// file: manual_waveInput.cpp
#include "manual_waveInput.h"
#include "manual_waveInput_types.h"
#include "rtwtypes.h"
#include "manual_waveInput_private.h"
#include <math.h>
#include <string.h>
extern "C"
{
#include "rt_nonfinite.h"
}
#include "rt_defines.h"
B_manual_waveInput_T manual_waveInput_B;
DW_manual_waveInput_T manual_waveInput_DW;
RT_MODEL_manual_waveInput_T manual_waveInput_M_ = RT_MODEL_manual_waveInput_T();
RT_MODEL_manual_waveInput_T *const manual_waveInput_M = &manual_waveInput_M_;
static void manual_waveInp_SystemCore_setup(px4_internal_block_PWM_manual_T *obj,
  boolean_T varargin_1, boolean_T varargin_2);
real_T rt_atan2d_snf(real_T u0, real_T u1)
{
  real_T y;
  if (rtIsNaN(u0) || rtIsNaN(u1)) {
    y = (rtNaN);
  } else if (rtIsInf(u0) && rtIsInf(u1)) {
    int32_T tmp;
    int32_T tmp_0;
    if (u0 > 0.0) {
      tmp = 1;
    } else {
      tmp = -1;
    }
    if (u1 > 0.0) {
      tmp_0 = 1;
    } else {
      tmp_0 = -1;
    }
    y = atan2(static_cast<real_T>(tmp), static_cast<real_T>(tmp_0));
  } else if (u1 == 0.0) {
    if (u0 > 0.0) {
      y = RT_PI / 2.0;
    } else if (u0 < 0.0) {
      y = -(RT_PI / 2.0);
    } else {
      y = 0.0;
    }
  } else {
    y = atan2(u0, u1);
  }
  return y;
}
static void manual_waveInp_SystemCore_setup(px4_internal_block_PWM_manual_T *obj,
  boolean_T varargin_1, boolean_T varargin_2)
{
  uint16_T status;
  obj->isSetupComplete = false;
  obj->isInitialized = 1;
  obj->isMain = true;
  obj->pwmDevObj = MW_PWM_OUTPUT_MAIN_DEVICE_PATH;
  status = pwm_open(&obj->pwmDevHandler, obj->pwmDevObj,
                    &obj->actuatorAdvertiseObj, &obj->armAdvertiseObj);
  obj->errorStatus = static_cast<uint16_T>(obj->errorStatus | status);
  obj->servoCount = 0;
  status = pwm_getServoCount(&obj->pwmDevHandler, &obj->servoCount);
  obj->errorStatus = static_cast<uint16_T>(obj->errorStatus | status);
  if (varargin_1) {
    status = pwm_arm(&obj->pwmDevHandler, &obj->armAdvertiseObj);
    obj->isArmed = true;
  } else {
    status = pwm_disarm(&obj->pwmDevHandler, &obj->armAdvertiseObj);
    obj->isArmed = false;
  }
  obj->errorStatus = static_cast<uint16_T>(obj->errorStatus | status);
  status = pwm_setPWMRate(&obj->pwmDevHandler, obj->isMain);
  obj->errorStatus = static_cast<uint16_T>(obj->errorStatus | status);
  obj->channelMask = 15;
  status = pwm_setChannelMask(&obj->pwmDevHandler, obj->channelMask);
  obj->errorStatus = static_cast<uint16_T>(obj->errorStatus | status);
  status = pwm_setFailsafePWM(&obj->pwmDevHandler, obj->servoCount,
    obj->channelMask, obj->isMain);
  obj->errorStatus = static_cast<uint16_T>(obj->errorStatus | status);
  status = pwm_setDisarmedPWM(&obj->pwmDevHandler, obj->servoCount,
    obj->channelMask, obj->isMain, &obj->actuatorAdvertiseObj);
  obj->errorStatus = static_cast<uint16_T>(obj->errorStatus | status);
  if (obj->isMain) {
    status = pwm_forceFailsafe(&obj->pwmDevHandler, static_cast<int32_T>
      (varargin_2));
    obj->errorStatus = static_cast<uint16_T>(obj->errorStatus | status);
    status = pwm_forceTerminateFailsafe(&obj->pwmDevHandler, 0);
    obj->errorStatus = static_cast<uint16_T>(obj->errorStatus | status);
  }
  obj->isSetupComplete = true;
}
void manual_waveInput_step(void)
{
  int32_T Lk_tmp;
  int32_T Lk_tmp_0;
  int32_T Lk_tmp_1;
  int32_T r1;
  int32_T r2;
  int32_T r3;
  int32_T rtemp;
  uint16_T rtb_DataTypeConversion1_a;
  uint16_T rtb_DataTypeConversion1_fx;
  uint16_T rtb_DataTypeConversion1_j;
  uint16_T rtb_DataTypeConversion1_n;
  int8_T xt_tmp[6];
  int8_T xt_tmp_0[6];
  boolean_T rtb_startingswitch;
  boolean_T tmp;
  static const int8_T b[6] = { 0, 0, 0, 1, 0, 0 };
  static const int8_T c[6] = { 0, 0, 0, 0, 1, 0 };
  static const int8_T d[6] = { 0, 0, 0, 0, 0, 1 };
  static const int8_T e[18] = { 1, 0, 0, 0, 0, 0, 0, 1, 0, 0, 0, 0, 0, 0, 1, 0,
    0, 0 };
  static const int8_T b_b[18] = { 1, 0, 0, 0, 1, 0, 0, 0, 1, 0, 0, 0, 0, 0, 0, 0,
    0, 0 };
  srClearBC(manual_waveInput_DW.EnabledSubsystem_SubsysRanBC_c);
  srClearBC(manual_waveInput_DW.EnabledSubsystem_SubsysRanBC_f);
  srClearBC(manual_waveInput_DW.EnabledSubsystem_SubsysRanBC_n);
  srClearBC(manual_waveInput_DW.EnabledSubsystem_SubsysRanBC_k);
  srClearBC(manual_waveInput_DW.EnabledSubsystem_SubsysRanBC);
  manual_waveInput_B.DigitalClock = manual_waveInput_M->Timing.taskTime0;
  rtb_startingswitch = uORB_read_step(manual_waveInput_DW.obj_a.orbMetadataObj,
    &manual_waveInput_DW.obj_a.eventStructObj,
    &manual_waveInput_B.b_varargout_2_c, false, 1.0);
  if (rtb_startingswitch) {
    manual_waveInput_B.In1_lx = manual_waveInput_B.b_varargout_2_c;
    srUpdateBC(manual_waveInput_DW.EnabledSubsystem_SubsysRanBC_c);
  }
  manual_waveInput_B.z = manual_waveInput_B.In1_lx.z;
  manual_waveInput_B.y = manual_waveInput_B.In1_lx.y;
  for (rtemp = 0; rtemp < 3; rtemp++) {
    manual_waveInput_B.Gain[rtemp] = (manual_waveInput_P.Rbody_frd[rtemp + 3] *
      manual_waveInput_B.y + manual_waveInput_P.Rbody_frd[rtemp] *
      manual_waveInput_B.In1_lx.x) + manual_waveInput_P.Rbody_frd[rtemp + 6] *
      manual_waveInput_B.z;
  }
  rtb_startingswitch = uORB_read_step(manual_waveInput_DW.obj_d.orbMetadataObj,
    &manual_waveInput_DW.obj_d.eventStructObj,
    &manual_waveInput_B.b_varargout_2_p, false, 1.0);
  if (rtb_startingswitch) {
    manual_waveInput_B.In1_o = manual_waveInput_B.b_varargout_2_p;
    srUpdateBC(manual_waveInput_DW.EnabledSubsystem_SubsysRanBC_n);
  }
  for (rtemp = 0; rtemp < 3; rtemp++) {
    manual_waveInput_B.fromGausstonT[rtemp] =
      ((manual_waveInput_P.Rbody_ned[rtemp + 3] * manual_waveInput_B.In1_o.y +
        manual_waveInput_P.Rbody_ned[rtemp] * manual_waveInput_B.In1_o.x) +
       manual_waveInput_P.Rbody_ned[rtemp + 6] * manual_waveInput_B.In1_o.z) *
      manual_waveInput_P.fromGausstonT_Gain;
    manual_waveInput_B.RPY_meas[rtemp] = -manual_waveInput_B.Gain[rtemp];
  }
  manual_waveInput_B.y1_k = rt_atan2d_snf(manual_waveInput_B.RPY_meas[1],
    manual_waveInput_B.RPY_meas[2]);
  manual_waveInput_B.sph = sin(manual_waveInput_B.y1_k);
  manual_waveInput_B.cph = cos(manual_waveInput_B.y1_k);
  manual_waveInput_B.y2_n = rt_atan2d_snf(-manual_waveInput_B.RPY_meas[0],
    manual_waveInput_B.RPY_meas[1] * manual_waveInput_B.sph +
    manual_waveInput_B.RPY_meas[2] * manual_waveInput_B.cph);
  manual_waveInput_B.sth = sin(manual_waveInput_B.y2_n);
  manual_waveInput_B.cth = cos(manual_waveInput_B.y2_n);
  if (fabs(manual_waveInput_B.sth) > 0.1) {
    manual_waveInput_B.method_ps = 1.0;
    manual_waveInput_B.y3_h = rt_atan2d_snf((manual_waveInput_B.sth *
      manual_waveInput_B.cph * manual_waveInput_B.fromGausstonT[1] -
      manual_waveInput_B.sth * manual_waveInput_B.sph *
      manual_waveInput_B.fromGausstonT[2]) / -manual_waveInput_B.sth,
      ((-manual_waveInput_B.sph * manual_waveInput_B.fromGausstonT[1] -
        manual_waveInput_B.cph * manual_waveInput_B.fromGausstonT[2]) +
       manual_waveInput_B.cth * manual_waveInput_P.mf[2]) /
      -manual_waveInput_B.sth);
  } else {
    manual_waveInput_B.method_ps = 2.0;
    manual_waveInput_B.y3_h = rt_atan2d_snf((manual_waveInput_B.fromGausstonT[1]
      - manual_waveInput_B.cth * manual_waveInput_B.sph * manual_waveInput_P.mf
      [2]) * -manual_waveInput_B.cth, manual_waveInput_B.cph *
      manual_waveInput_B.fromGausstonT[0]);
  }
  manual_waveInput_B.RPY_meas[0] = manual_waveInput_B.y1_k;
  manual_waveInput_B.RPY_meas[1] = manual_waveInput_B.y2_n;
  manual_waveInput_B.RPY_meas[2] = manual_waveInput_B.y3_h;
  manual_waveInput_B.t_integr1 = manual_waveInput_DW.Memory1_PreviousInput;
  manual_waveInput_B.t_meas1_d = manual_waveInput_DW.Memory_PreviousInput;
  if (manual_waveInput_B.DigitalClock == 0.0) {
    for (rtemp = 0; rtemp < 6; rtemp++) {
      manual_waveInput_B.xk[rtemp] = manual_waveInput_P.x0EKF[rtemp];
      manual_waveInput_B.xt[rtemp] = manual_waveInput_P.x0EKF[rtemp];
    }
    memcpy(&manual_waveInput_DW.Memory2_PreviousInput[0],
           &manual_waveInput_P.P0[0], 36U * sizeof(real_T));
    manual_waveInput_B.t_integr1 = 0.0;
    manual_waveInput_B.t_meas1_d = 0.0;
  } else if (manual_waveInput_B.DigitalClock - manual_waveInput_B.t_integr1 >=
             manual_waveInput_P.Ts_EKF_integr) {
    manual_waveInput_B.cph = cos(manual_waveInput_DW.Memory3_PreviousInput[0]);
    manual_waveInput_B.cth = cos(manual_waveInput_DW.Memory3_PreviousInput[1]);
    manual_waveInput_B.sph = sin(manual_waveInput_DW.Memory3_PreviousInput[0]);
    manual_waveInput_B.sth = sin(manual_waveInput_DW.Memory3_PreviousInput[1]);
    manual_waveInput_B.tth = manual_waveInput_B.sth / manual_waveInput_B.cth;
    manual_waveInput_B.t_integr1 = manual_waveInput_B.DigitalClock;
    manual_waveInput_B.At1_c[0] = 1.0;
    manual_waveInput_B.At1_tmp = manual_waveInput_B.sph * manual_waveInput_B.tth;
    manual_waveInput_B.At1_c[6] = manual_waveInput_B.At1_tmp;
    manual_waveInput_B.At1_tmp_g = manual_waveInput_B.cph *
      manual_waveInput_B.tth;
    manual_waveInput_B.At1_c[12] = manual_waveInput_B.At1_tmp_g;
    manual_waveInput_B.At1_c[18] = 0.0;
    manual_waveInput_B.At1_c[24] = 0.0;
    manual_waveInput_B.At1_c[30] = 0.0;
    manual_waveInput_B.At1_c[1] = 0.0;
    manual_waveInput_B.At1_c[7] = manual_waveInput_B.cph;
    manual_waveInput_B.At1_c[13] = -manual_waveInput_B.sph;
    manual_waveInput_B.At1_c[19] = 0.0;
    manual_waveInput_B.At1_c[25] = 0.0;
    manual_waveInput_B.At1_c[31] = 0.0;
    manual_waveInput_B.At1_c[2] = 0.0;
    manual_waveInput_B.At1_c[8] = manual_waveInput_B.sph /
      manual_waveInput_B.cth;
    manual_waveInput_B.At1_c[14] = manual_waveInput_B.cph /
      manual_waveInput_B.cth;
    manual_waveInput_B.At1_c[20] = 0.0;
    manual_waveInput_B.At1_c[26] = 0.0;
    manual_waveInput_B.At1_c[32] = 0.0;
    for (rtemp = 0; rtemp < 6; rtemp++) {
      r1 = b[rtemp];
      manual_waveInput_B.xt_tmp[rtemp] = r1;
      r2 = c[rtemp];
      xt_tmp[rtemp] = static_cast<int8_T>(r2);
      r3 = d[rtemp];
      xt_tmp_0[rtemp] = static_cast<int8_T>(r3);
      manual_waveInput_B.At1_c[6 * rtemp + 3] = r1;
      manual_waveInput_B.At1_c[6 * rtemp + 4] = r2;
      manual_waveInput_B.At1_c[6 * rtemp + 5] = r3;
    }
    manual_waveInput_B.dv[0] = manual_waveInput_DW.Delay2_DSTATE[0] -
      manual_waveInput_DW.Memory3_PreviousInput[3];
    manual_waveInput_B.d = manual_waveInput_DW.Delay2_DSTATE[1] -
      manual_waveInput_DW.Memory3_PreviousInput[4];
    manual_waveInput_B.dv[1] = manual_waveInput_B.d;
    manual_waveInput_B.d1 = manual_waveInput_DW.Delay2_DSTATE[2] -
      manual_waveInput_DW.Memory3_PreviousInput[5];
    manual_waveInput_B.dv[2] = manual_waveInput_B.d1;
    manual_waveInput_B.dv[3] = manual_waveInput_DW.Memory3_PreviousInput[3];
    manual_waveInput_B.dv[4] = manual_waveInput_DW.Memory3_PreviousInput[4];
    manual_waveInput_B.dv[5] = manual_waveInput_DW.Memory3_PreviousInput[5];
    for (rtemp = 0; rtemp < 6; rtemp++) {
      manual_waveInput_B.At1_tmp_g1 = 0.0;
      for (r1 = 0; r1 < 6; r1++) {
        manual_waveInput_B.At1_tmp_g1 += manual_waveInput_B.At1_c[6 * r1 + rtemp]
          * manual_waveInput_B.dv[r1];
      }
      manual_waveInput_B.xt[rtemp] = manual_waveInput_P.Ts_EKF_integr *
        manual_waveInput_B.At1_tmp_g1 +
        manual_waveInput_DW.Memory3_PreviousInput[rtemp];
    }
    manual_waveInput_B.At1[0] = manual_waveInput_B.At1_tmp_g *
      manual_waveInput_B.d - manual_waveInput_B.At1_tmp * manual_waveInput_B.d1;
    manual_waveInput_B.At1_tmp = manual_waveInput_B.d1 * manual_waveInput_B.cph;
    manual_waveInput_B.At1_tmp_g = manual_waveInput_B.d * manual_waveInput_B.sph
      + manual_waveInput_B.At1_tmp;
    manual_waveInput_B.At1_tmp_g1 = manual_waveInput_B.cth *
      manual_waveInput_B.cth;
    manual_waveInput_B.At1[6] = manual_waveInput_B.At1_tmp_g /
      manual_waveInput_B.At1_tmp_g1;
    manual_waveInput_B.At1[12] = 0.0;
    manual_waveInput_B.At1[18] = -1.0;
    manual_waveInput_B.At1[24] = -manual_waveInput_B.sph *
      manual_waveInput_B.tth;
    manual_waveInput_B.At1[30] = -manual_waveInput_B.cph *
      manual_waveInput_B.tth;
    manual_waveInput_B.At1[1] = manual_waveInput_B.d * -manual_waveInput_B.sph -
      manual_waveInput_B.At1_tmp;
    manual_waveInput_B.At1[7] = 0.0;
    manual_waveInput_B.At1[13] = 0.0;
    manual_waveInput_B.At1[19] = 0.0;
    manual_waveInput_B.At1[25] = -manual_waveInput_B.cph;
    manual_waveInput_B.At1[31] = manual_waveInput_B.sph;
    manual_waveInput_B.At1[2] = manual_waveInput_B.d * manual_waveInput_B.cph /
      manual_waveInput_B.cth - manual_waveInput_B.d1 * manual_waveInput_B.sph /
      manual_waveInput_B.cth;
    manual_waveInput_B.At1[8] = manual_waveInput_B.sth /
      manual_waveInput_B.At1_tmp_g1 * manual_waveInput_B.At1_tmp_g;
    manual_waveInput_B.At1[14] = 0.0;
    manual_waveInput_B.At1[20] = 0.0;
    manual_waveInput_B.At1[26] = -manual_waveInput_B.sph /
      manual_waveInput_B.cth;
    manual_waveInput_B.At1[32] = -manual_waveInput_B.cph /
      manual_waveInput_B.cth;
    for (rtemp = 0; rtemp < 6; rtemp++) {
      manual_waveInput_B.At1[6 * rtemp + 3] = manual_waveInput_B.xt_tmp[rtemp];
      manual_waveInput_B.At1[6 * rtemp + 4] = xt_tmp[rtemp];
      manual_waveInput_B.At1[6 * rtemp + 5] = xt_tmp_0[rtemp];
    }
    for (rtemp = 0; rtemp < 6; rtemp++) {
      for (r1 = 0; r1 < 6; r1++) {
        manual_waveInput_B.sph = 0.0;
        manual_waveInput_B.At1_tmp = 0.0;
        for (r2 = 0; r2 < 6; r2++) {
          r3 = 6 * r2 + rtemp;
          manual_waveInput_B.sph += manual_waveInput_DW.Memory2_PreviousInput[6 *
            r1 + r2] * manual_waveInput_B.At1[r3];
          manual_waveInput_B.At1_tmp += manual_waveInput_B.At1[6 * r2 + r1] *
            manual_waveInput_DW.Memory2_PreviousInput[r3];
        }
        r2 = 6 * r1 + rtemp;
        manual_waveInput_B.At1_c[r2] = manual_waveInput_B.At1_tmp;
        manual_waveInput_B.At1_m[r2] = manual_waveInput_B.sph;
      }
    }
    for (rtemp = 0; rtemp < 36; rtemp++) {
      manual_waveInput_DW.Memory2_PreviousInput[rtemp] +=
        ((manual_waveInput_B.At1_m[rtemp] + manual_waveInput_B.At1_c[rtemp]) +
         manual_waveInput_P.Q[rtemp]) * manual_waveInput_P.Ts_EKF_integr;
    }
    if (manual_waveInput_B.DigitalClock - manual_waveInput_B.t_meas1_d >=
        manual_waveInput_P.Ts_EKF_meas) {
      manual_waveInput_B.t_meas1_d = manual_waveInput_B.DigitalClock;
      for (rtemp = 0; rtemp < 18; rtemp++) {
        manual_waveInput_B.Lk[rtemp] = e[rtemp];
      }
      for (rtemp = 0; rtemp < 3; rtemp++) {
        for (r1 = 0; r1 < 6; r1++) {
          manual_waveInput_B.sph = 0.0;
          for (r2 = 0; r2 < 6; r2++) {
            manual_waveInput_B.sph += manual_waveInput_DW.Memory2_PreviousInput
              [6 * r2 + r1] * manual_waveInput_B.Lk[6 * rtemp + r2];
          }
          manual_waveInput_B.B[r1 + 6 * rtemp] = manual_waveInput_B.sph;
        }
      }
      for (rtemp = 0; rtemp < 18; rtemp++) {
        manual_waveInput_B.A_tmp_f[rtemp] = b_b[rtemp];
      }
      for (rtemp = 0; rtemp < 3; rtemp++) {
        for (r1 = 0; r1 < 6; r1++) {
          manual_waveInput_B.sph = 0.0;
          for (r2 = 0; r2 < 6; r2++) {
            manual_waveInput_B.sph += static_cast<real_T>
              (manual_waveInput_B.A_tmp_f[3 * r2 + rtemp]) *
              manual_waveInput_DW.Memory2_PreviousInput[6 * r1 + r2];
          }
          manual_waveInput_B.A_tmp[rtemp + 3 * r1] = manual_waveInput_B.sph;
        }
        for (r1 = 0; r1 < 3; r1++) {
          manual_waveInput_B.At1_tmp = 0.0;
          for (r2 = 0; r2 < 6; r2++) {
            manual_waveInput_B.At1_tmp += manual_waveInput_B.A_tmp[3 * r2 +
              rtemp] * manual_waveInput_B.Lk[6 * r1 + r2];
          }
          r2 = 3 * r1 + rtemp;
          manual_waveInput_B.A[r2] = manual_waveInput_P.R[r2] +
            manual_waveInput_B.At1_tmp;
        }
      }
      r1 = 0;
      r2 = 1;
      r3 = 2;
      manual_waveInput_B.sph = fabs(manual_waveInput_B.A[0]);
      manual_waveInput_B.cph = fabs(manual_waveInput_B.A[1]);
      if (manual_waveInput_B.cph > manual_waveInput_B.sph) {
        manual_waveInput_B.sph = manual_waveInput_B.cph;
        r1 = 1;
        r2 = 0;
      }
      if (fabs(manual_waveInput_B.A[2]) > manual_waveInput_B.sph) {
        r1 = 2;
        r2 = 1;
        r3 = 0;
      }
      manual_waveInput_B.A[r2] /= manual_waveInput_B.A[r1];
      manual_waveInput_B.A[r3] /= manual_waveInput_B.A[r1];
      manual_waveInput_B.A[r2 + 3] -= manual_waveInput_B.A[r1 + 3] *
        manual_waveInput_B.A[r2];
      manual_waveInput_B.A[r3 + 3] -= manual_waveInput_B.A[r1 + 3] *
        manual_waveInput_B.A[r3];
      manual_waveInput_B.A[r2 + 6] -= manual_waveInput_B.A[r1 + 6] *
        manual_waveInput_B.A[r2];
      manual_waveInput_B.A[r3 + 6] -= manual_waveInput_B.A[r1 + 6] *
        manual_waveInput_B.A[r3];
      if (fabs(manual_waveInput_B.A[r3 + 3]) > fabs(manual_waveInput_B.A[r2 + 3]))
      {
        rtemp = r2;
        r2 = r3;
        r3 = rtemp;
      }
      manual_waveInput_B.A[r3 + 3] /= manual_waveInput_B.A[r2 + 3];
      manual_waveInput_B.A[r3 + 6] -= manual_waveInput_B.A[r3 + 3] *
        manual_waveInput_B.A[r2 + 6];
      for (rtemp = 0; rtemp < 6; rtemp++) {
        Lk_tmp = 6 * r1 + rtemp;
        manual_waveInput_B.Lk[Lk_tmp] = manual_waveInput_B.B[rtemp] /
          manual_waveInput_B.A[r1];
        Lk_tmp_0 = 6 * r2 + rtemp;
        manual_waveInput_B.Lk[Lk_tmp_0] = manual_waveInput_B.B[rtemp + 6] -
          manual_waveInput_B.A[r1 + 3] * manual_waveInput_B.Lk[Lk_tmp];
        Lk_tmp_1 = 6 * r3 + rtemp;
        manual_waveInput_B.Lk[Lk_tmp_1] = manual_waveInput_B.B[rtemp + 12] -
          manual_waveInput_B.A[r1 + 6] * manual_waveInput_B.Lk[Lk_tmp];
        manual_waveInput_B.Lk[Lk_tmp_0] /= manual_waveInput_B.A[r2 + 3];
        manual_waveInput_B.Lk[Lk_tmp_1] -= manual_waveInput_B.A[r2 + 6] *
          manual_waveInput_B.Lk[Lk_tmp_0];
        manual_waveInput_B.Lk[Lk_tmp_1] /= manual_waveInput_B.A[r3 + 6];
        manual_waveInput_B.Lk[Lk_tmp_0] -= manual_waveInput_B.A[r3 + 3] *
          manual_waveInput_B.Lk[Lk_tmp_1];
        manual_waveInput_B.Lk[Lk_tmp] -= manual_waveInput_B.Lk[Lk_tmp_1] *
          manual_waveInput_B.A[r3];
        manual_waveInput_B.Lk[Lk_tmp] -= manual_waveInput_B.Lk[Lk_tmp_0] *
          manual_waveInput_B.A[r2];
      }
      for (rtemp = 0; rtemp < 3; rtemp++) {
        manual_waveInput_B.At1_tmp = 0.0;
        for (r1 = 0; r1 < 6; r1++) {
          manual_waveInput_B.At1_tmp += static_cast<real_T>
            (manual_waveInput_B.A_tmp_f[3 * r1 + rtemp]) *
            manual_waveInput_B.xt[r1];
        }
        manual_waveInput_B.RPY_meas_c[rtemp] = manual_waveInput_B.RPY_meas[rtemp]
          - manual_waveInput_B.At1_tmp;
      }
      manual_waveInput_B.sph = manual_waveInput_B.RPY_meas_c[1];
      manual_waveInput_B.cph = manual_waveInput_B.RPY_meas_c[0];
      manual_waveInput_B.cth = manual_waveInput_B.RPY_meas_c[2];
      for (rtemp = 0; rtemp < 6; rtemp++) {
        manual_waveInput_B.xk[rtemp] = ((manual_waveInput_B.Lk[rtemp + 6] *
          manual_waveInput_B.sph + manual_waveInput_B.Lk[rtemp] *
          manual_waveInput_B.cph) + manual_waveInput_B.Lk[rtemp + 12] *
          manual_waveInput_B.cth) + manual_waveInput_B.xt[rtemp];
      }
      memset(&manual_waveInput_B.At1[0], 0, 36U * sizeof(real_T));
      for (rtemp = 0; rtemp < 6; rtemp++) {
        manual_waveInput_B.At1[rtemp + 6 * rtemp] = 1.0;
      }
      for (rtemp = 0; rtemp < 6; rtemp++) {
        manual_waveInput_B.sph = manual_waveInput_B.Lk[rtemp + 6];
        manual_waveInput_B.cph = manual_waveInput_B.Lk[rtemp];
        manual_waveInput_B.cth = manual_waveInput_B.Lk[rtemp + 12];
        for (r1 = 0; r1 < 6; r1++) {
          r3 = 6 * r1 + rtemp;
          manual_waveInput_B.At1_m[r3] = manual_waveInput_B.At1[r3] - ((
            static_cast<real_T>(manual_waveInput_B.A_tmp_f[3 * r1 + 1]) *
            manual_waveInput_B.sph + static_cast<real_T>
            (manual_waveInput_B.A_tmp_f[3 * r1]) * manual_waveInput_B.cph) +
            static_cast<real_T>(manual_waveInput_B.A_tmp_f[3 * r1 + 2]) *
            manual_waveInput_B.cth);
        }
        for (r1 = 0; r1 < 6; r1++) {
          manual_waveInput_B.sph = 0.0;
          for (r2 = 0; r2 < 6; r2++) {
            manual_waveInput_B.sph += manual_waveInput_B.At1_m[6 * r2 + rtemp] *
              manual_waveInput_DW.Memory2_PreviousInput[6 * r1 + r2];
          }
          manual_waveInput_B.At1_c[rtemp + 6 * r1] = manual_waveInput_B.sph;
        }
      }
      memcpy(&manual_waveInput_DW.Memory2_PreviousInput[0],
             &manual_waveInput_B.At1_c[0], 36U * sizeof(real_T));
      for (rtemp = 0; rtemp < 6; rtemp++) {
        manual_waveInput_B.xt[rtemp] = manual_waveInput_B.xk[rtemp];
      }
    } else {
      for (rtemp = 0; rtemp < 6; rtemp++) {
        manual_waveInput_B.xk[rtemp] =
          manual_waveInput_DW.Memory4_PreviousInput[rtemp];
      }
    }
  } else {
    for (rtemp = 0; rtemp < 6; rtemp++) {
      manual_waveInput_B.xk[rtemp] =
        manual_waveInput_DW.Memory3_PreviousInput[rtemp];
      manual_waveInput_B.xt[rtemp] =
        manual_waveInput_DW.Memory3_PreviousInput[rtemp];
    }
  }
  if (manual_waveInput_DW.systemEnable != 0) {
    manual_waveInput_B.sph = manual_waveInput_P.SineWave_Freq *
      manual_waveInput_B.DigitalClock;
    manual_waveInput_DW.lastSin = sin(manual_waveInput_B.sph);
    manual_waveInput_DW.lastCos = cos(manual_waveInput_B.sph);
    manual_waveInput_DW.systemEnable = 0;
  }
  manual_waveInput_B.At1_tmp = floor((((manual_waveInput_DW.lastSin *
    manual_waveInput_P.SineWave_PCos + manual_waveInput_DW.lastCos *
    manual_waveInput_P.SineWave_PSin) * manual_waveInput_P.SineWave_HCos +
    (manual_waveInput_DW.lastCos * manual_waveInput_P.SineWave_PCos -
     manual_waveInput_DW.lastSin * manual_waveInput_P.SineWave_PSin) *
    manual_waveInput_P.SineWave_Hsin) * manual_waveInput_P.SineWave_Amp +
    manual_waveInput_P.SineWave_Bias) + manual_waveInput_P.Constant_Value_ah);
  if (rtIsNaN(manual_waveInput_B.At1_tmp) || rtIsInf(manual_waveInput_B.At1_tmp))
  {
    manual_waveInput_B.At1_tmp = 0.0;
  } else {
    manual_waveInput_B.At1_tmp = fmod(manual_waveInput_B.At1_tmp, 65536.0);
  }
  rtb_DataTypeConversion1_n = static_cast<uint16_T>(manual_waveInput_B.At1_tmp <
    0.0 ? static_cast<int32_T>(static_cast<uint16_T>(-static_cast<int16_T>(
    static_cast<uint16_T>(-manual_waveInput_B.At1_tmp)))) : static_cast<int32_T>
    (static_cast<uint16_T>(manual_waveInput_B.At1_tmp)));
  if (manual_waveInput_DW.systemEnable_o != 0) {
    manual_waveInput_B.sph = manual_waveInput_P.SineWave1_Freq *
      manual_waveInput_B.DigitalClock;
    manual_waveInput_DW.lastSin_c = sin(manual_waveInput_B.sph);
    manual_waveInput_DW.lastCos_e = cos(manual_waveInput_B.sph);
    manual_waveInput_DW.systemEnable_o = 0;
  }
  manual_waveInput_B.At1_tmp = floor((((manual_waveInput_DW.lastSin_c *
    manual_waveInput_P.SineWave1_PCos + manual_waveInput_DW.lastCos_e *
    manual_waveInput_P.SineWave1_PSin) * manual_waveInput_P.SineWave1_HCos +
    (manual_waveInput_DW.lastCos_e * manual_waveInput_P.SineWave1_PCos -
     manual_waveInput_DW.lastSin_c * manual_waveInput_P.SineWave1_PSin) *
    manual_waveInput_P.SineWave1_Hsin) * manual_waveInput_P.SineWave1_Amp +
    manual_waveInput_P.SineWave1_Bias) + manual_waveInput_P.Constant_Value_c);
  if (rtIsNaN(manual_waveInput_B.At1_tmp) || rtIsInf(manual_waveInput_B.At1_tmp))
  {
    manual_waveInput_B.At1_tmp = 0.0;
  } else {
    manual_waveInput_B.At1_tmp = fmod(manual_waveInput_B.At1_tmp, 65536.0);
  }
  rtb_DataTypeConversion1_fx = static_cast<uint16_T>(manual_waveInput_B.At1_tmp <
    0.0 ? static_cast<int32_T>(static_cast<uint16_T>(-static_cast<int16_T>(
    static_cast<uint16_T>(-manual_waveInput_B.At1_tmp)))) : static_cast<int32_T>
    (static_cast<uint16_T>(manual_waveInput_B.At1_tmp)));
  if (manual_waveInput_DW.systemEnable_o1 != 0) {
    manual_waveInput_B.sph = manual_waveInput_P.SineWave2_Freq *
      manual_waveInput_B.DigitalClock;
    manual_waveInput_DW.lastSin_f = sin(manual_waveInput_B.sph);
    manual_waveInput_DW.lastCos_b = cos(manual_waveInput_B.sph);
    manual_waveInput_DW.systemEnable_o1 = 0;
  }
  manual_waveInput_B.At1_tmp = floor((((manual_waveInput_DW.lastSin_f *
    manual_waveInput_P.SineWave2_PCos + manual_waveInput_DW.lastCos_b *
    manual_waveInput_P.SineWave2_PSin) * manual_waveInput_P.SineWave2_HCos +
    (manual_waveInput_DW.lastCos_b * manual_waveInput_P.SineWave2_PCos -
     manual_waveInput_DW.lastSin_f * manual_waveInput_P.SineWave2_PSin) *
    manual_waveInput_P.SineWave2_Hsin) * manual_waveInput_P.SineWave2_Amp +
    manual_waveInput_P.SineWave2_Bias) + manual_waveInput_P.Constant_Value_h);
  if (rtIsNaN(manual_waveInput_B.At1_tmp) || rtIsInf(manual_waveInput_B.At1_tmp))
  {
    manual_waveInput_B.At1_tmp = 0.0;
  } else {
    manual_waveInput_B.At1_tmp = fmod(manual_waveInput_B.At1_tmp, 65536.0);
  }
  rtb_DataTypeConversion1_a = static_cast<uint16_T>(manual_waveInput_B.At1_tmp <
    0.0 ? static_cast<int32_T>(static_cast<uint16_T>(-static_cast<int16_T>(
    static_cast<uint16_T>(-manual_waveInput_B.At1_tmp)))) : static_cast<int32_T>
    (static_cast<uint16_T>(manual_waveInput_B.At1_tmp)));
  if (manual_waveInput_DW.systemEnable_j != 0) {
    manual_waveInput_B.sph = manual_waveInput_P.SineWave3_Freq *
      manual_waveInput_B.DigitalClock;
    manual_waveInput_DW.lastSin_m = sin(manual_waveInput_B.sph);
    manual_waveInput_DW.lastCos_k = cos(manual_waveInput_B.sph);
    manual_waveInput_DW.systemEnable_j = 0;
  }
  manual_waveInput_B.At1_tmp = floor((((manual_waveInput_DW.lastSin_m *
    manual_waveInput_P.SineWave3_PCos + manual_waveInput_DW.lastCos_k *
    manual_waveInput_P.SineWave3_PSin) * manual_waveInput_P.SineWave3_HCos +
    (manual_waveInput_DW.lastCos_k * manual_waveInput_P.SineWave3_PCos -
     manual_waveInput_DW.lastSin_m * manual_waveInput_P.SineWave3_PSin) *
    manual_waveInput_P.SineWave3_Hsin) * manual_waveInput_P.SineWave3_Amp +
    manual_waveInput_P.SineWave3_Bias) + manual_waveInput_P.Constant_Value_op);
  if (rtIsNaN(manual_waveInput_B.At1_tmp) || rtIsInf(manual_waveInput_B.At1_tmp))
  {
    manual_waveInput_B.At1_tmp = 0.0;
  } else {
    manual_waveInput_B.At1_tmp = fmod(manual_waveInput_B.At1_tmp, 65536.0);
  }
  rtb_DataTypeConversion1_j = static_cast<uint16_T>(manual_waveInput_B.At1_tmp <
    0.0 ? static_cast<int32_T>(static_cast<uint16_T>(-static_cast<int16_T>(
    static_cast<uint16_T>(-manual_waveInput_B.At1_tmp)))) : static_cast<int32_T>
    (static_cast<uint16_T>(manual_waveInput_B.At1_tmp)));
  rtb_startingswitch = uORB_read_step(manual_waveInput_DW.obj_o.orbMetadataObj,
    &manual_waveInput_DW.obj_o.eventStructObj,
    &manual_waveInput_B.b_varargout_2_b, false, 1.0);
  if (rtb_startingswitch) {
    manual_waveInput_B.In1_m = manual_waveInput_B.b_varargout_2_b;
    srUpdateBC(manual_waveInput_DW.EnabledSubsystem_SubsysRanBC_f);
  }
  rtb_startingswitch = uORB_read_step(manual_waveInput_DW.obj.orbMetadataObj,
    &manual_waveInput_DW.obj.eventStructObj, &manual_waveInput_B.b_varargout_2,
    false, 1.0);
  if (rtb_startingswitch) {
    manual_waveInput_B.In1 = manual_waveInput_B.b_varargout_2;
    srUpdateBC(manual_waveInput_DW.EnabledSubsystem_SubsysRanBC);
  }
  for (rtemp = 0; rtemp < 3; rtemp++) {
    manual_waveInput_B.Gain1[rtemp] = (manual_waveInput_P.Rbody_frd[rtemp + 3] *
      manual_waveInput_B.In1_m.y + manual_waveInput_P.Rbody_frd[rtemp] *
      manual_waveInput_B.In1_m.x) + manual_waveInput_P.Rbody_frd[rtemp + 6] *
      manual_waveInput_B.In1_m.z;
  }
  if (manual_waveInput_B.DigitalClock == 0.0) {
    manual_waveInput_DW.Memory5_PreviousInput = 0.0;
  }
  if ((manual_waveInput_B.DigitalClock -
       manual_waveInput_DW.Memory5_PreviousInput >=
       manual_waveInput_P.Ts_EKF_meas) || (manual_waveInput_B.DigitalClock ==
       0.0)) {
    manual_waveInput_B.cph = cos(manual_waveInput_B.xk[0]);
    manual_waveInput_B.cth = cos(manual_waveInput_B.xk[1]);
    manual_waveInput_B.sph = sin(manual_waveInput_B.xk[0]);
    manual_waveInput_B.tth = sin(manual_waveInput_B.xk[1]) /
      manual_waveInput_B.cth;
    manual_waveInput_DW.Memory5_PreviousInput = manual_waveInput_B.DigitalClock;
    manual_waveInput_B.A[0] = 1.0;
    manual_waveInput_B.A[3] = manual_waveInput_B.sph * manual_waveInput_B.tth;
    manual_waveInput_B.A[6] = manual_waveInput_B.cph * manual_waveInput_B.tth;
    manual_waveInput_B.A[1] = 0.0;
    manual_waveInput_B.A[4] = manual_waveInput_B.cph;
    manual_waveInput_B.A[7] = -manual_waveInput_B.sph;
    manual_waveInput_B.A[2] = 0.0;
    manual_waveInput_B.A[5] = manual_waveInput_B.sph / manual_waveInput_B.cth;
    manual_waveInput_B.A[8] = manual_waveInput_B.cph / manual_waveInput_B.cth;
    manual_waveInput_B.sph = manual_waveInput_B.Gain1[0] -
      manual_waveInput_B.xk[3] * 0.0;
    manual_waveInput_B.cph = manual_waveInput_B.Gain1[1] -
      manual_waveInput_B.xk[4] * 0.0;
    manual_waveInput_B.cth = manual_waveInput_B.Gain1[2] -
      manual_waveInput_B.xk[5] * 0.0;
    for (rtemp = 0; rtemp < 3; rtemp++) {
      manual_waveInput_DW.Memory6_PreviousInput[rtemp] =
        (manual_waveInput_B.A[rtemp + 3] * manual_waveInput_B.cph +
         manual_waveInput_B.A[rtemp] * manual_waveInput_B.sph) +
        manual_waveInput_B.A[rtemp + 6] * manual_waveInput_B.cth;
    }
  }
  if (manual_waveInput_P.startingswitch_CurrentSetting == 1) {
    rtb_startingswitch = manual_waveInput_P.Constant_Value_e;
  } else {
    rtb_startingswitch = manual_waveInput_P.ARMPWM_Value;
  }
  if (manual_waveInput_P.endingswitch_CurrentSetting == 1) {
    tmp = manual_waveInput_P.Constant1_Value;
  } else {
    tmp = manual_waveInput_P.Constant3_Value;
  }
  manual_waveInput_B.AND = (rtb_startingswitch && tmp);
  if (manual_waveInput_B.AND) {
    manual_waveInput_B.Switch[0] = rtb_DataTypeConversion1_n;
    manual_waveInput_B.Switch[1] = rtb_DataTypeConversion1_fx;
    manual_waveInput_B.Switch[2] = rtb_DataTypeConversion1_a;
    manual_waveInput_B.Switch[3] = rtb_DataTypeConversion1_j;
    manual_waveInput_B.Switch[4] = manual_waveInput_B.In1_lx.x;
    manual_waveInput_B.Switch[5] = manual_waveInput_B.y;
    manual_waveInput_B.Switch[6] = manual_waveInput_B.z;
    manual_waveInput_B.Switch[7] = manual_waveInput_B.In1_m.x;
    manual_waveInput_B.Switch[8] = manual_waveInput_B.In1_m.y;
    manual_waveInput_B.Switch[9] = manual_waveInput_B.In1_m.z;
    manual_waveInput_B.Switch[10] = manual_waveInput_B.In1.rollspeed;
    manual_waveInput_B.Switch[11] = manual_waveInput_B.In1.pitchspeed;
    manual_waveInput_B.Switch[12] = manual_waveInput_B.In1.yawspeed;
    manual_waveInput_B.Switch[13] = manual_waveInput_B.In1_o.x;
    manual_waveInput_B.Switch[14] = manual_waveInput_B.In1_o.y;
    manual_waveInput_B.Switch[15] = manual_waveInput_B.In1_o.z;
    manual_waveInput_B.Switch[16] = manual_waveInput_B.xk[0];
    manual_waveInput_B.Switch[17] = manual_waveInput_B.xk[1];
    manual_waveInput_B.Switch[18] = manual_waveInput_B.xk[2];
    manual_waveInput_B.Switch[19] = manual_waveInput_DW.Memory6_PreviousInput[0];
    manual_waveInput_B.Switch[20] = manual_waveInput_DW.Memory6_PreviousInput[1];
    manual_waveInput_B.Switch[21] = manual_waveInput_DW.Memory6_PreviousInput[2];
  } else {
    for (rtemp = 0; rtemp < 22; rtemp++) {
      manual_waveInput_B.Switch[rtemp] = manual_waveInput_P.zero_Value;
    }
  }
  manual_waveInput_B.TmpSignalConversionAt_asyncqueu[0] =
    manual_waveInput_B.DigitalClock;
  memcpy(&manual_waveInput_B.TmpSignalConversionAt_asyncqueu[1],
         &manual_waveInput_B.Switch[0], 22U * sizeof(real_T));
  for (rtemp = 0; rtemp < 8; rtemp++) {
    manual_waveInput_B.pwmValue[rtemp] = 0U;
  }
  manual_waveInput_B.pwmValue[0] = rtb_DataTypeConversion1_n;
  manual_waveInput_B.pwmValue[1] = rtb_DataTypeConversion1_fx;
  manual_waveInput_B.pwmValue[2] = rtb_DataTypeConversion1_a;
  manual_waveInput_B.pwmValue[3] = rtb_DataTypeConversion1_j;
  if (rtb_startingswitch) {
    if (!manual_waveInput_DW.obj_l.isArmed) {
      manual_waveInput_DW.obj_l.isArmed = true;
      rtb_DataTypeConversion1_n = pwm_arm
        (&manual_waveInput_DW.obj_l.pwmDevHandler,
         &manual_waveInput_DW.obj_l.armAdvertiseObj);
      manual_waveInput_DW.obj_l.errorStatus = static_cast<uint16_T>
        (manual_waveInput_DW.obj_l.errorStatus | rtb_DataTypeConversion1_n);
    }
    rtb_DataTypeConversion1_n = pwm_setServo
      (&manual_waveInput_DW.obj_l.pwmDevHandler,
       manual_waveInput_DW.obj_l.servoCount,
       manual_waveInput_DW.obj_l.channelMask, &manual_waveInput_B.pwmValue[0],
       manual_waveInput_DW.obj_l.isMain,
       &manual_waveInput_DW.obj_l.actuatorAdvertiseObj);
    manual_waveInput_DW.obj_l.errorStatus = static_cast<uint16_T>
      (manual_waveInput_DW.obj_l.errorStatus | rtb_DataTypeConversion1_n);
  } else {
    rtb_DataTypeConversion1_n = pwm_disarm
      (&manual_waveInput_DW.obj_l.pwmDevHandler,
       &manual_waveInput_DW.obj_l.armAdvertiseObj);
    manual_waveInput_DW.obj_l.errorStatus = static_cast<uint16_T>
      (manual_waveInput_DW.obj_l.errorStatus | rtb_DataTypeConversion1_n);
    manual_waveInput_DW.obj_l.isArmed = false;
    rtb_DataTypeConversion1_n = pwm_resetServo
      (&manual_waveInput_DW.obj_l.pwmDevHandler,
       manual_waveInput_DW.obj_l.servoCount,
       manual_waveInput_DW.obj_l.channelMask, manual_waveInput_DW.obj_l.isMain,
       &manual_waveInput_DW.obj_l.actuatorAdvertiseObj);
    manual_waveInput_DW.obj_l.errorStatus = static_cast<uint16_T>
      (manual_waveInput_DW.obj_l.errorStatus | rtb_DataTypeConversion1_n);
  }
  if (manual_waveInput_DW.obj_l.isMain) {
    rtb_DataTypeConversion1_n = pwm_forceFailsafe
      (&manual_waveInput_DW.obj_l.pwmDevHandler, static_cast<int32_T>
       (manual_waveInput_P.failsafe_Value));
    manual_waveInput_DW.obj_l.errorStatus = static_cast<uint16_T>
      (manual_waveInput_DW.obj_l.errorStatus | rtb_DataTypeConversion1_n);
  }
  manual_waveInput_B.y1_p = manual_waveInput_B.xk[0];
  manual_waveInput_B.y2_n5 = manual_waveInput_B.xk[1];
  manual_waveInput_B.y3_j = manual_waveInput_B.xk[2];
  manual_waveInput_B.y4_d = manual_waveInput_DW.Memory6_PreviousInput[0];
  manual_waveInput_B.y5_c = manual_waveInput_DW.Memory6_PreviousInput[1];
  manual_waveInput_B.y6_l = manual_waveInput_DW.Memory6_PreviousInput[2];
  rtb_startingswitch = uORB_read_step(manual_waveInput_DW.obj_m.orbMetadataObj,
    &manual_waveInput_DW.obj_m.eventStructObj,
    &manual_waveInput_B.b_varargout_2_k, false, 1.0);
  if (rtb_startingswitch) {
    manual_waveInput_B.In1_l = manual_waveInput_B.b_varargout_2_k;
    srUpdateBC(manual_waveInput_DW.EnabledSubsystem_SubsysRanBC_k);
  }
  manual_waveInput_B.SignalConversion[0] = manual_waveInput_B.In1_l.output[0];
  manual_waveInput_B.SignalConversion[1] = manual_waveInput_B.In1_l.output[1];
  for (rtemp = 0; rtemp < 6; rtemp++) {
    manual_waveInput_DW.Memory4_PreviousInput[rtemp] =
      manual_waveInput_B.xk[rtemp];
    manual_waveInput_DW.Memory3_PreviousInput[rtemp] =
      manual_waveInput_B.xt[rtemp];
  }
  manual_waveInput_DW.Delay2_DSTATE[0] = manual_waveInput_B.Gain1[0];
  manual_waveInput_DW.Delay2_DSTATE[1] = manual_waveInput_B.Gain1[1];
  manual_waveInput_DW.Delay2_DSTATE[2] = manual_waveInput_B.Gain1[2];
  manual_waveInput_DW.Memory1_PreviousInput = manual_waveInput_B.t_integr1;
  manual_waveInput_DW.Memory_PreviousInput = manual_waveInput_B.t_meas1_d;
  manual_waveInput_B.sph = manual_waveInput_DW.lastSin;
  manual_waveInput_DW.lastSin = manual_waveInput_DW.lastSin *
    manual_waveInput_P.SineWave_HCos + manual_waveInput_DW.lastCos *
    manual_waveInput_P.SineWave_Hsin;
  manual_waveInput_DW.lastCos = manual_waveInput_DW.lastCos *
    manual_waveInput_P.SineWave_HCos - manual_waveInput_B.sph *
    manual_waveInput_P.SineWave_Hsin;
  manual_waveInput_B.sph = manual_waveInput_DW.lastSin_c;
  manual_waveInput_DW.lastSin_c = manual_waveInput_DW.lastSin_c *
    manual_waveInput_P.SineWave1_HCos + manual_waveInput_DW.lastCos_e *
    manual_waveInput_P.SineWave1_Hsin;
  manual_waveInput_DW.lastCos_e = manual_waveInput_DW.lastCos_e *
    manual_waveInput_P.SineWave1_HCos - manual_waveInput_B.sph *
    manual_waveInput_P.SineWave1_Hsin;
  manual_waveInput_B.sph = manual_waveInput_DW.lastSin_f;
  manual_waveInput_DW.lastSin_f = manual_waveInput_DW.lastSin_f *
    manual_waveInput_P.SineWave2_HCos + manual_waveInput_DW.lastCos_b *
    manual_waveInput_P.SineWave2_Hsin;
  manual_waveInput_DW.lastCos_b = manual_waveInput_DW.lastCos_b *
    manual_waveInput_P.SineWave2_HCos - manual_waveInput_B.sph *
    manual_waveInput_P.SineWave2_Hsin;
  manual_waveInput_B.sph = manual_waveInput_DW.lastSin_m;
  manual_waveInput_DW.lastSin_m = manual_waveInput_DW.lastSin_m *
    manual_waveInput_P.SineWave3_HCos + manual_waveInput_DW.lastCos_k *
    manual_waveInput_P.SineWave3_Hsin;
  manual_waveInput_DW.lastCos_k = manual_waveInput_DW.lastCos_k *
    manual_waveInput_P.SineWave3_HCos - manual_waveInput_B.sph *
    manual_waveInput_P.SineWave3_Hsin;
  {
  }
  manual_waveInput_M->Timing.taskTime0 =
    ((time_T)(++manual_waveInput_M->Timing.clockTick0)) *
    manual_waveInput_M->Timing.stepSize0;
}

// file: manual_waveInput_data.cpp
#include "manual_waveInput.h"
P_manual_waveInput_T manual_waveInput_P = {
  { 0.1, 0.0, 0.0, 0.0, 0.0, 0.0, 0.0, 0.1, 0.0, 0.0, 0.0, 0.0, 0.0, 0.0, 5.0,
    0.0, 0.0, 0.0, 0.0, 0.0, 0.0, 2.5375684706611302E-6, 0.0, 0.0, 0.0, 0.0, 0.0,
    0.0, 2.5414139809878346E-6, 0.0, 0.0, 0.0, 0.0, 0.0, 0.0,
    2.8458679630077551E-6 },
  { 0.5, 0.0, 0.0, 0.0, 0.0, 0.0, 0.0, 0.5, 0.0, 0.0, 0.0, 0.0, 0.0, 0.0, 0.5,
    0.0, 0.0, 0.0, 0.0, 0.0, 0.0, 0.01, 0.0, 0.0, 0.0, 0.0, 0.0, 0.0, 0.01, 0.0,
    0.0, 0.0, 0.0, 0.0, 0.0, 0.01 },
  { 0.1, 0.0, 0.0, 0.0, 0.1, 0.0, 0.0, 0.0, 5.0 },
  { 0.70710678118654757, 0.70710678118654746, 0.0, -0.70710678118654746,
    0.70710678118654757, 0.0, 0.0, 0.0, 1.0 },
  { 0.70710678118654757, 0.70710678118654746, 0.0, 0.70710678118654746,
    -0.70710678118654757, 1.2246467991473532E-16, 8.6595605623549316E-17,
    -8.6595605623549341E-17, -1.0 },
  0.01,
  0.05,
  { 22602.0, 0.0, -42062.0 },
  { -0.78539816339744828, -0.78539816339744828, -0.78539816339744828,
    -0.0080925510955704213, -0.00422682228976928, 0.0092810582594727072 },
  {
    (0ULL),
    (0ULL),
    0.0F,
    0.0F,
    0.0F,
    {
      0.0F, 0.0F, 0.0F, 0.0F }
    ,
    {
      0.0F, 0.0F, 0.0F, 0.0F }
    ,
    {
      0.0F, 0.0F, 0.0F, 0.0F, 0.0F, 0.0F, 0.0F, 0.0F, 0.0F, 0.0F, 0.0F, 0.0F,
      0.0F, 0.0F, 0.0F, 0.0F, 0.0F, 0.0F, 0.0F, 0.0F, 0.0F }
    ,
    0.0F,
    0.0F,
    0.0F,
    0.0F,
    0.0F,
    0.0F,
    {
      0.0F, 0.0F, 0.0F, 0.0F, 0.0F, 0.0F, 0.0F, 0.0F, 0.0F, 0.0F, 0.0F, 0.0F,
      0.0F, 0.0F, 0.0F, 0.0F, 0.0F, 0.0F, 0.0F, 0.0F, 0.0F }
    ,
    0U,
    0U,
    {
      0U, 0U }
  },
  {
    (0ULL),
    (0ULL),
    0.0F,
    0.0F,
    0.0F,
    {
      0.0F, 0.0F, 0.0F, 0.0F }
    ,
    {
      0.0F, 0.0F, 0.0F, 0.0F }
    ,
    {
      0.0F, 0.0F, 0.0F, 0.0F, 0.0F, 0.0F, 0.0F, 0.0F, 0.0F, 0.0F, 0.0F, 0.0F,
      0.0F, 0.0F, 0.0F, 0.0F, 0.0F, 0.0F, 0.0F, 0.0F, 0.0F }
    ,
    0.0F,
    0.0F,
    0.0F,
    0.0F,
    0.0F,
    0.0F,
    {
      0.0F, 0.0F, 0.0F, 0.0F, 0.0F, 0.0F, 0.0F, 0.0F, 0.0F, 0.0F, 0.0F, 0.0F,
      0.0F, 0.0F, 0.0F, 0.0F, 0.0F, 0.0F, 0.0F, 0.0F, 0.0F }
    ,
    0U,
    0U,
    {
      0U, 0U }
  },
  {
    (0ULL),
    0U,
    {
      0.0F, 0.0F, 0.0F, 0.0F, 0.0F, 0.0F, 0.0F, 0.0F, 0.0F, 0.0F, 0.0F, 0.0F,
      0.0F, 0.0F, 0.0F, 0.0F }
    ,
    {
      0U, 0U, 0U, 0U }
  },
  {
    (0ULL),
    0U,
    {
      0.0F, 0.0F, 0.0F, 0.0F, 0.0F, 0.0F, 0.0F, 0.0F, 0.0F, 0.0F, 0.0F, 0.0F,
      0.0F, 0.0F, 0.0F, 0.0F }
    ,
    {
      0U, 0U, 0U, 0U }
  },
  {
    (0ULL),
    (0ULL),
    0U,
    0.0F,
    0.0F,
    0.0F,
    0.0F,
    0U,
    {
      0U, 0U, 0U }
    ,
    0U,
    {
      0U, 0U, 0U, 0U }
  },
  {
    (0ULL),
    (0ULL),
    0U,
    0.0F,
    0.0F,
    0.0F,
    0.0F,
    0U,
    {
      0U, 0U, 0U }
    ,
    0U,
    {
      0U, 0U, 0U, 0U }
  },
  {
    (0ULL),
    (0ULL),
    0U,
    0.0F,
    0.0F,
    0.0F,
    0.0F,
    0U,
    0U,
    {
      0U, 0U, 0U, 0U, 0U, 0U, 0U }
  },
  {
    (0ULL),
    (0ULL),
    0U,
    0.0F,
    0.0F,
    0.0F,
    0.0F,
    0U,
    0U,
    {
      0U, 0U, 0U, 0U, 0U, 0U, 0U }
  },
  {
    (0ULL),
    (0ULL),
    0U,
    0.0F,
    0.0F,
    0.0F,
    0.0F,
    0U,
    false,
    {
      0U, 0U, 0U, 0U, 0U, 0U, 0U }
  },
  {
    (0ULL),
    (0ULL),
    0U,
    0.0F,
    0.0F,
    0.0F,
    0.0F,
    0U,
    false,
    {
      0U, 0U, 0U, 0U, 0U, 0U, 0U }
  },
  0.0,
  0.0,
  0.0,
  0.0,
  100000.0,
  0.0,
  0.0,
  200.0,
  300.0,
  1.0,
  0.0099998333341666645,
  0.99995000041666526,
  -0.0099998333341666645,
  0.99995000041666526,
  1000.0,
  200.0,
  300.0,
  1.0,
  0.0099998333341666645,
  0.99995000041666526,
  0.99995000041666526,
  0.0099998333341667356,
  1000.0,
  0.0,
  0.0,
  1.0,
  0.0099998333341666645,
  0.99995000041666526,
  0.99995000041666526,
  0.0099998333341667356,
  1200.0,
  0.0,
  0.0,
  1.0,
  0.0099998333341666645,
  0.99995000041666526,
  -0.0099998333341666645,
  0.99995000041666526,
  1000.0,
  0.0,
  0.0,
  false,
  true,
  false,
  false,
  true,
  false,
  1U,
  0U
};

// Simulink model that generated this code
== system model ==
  DigitalClock : DigitalClock
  MATLABFunction#1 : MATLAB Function  <- 1: MATLABFunction#2
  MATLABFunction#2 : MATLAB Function  <- 1: Gain, 2: fromGausstonT, 3: Constant#1
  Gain : Gain  Gain=Rbody_frd  Multiplication=Matrix(K*u) (u vector)  <- 1: DataTypeConversion#1
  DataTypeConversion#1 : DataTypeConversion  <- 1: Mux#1
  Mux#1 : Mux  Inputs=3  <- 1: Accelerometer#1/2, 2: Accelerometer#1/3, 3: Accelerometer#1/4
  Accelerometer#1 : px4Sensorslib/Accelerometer
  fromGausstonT : Gain  Gain=100000  <- 1: Gain#1
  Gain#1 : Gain  Gain=Rbody_ned  Multiplication=Matrix(K*u) (u vector)  <- 1: DataTypeConversion#2
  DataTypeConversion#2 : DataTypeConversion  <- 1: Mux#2
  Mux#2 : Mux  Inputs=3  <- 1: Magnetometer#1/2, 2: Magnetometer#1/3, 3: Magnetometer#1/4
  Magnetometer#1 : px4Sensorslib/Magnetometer
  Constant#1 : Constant  Value=mf
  Switch : Switch  Criteria=u2 > Threshold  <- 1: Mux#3, 2: AND, 3: zero
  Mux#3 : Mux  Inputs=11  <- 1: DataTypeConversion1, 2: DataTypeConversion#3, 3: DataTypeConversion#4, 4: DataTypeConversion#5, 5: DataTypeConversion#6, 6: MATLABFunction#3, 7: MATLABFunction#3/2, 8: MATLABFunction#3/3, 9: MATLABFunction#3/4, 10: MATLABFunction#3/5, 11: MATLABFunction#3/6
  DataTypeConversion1 : DataTypeConversion  <- 1: DataTypeConversion#7
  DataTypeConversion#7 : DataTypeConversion  <- 1: Sum#1
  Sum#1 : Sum  Inputs=++  <- 1: SineWave, 2: Constant
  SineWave : Sin  Amplitude=200  Bias=300
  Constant : Constant  Value=1000
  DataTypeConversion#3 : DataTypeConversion  <- 1: DataTypeConversion#8
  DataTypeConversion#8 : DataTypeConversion  <- 1: Sum#2
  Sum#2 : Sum  Inputs=++  <- 1: SineWave1, 2: Constant#2
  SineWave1 : Sin  Amplitude=200  Bias=300  Phase=pi
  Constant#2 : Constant  Value=1000
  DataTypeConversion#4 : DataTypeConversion  <- 1: DataTypeConversion#9
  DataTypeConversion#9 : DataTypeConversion  <- 1: Sum#3
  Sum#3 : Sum  Inputs=++  <- 1: SineWave2, 2: Constant#3
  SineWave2 : Sin  Amplitude=200  Bias=300  Phase=pi/4
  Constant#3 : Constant  Value=1200
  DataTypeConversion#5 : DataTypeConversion  <- 1: DataTypeConversion#10
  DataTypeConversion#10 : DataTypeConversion  <- 1: Sum#4
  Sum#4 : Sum  Inputs=++  <- 1: SineWave3, 2: Constant#4
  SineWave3 : Sin  Amplitude=200  Bias=300  Phase=pi/4+pi
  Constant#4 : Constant  Value=1000
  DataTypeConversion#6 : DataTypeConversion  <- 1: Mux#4
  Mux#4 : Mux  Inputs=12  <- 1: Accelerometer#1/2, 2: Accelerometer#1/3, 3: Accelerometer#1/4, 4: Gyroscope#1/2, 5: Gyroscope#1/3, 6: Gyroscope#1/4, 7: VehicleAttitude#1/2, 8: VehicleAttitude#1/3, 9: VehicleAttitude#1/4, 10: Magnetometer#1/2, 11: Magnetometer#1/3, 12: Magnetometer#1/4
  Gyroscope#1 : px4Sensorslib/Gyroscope
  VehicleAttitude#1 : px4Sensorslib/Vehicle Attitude
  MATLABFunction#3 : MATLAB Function  <- 1: DataTypeConversion#11
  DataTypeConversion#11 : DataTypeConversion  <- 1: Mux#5
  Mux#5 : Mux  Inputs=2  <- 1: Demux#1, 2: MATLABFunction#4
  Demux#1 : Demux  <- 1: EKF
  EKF : MATLAB Function  <- 1: DigitalClock#1, 2: Memory4, 3: Memory3, 4: Memory2, 5: Delay2, 6: MATLABFunction#2, 7: Constant#5, 8: Constant3, 9: Constant#6, 10: Constant#7, 11: Constant#8, 12: Constant1, 13: Memory1, 14: Memory
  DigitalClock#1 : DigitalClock
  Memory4 : Memory  <- 1: EKF
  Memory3 : Memory  <- 1: EKF/2
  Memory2 : Memory  <- 1: EKF/3
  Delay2 : Delay  DelayLength=1  <- 1: Gain1
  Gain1 : Gain  Gain=Rbody_frd  Multiplication=Matrix(K*u) (u vector)  <- 1: DataTypeConversion#12
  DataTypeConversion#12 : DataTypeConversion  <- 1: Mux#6
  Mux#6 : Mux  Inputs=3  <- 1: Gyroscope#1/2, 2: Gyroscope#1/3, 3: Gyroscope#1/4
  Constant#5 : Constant  Value=x0EKF
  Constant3 : Constant  Value=P0
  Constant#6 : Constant  Value=Q
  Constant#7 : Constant  Value=R
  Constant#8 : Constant  Value=Ts_EKF_integr
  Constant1 : Constant  Value=Ts_EKF_meas
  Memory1 : Memory  <- 1: EKF/4
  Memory : Memory  <- 1: EKF/5
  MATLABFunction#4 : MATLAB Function  <- 1: DigitalClock#2, 2: EKF, 3: Gain1, 4: Constant#9, 5: Memory6, 6: Memory5
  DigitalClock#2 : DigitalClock
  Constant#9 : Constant  Value=Ts_EKF_meas
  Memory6 : Memory  <- 1: MATLABFunction#4
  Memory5 : Memory  <- 1: MATLABFunction#4/2
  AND : Logic  <- 1: startingswitch, 2: endingswitch
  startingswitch : ManualSwitch  <- 1: Constant#10, 2: ARMPWM
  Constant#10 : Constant  Value=0
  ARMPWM : Constant
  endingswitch : ManualSwitch  <- 1: Constant#11, 2: Constant#12
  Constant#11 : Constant
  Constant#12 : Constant  Value=0
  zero : Constant  Value=0
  MATLABFunction#5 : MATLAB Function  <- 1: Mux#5
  PX4PWMOutput#1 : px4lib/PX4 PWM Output  <- 1: startingswitch, 2: failsafe, 3: DataTypeConversion#7, 4: DataTypeConversion#8, 5: DataTypeConversion#9, 6: DataTypeConversion#10
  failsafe : Constant  Value=0
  SignalConversion : SignalConversion  <- 1: Selector#1
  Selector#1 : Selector  Indices=[1 2]  <- 1: BusSelector#1
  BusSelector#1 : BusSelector  <- 1: PX4uORBRead#1/2
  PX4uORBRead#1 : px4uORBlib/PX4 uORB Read
== matlab function MATLABFunction#1 ==
function [y1,y2,y3] = fcn(u)

y1 = u(1);
y2 = u(2);
y3 = u(3);

== matlab function MATLAB Function ==
function [y1,y2,y3,y4,y5,y6] = fcn(u)

y1 = u(1);
y2 = u(2);
y3 = u(3);
y4 = u(4);
y5 = u(5);
y6 = u(6);

== matlab function MATLAB Function ==
function [y1,y2,y3,y4,y5,y6] = fcn(u)

y1 = u(1);
y2 = u(2);
y3 = u(3);
y4 = u(4);
y5 = u(5);
y6 = u(6);

== matlab function MATLABFunction#2 ==
function [RPY_meas,method_ps]   = RPY_computation(a_b,mf_b,mf)
% description:
% - a_b             = measured linear acceleration in body-frame
% - w_b             = measured angular velocity in body-frame
% - mf_b            = measured magnetic field in body-frame
% - mf              = measured magnetic field in body-inertia
% - a_b_disturbe    = linear velocity measurement-noise
% - w_b_disturbe    = angular velocity measurement-noise
% - mf_b_disturbe   = magnetic field measurement-noise

% -------------------------------------------------------------------------------------------
% observation: the following computation works only if the angles
% phi,theta,psy are withing angles (-pi/2,+pi/2) (this is an open set, pi/2 is excluded)
% -------------------------------------------------------------------------------------------

a_b = -1*a_b;       % need to adjust the sign to use atan2() function correctly
mf_u = mf(3,1);     % magnetic field in up direction (z-dir in inertia frame)

% phi computation
ph_meas = atan2(a_b(2), a_b(3));
sph = sin(ph_meas);
cph = cos(ph_meas);

% theta computation
th_meas = atan2(-a_b(1), (a_b(2)*sph + a_b(3)*cph));
sth = sin(th_meas);
cth = cos(th_meas);

% psi computation
if abs(sin(th_meas)) > 0.1  % sin(th) != 0 
    method_ps = 1;
    ps_meas_numerator   = (sth*cph*mf_b(2) - sth*sph*mf_b(3))/(-sth);       % don't modify
    ps_meas_denominator = (-sph*mf_b(2) - cph*mf_b(3) + cth*mf_u)/(-sth);   % don't modify
    ps_meas = atan2(ps_meas_numerator, ps_meas_denominator);
else                        % sin(th) == 0
    method_ps = 2;
    ps_meas_numerator   = (mf_b(2) - cth*sph*mf_u)*(-cth);
    ps_meas_denominator = cph*mf_b(1);
    ps_meas = atan2(ps_meas_numerator, ps_meas_denominator);
end
RPY_meas = [ph_meas;th_meas;ps_meas];

== matlab function EKF ==
function [xk,xt,Pt,t_integr1,t_meas1] = EKF(time,xk1,xt1,Pt1,w_b1,RPY_meas,x0,P0,Q,R,Ts_EKF_integr,Ts_EKF_meas,t_integr1,t_meas1)

if time == 0
    xk = x0;
    xt = x0;
    Pt = P0;
    t_integr1 = 0;
    t_meas1 = 0;
elseif time - t_integr1 >= Ts_EKF_integr
    wp          =       w_b1(1,1);        % p-dir of angular velocity w
    wq          =       w_b1(2,1);        % q-dir of angular velocity w
    wr          =       w_b1(3,1);        % r-dir of angular velocity w

    phi         =       xt1(1,1);         %  roll angle (rad)
    theta       =       xt1(2,1);         %  pitch angle (rad)
    psi         =       xt1(3,1);         %  yaw angle (rad)  
    bias_wp     =       xt1(4,1);         % bias of p-dir of angular velocity w
    bias_wq     =       xt1(5,1);         % bias of q-dir of angular velocity w
    bias_wr     =       xt1(6,1);         % bias of r-dir of angular velocity w

    cph         =       cos(phi);
    cth         =       cos(theta);
    cps         =       cos(psi);
    sph         =       sin(phi);
    sth         =       sin(theta);
    sps         =       sin(psi);
    tth         =       sth/cth;

    % integration step
    t_integr1 = time;
    Mf = [1,    sph*tth,    cph*tth,    0,  0,  0;
          0,    cph,        -sph,       0,  0,  0;
          0,    sph/cth,    cph/cth,    0,  0,  0;
          0,    0,          0,          1,  0,  0;
          0,    0,          0,          0,  1,  0;
          0,    0,          0,          0,  0,  1;];
    Z1 = [wp-bias_wp; wq-bias_wq; wr-bias_wr; bias_wp; bias_wq; bias_wr;];
    f = Mf*Z1;
    xt = xt1 + Ts_EKF_integr*f;

    A1 = [cph*tth*(wq-bias_wq)-sph*tth*(wr-bias_wr),(sph*(wq-bias_wq)+cph*(wr-bias_wr))/cth^2,  0,  -1, -sph*tth,   -cph*tth;];
    A2 = [-sph*(wq-bias_wq)-cph*(wr-bias_wr),   0,  0,  0,  -cph,   sph;];
    A3 = [cph*(wq-bias_wq)/cth-sph*(wr-bias_wr)/cth, (sth/cth^2)*(sph*(wq-bias_wq)+cph*(wr-bias_wr)),   0,  0,  -sph/cth,   -cph/cth;];
    A4 = [0,    0,  0,  1,  0,  0;];
    A5 = [0,    0,  0,  0,  1,  0;];
    A6 = [0,    0,  0,  0,  0,  1;];
    At1 = [A1; A2; A3; A4; A5; A6;];
    Pt = Pt1 + Ts_EKF_integr*(At1*Pt1 + Pt1*At1' + Q);

    % measurement step
    if time - t_meas1 >= Ts_EKF_meas
        t_meas1 = time;
        Ck = [eye(3),zeros(3,3)];
        Lk = Pt*Ck'/(Ck*Pt*Ck' + R);
        xk = xt + Lk*(RPY_meas - Ck*xt);
        Pk = (eye(6) - Lk*Ck)*Pt;

        xt = xk;    % becomes the new xt1
        Pt = Pk;    % becomes the new Pt1
    else
        xk = xk1;    % xk1
    end
else
    xk = xt1;
    xt = xt1;
    Pt = Pt1;
end
end

== matlab function MATLABFunction#4 ==
function [RPY_rate,t_meas1] = xk_dot_computation(time,xk,w_b,Ts_EKF_meas,RPY_rate1,t_meas1)
RPY_rate = zeros(3,1);
if time == 0
    t_meas1 = 0;
end
if time - t_meas1 >= Ts_EKF_meas || time == 0
    wp          =       w_b(1,1);        % p-dir of angular velocity w
    wq          =       w_b(2,1);        % q-dir of angular velocity w
    wr          =       w_b(3,1);        % r-dir of angular velocity w

    phi         =       xk(1,1);         %  roll angle (rad)
    theta       =       xk(2,1);         %  pitch angle (rad)
    psi         =       xk(3,1);         %  yaw angle (rad)  
    bias_wp     =       xk(4,1)*0;         % bias of p-dir of angular velocity w
    bias_wq     =       xk(5,1)*0;         % bias of q-dir of angular velocity w
    bias_wr     =       xk(6,1)*0;         % bias of r-dir of angular velocity w

    cph         =       cos(phi);
    cth         =       cos(theta);
    cps         =       cos(psi);
    sph         =       sin(phi);
    sth         =       sin(theta);
    sps         =       sin(psi);
    tth         =       sth/cth;

    % integration step
    t_meas1 = time;
    W_eta = [1,    sph*tth,    cph*tth;
             0,    cph,        -sph;
             0,    sph/cth,    cph/cth;];
    w_b_corrected = [wp-bias_wp; wq-bias_wq; wr-bias_wr;];
    RPY_rate = W_eta*w_b_corrected;
else
    RPY_rate = RPY_rate1;
end
end
